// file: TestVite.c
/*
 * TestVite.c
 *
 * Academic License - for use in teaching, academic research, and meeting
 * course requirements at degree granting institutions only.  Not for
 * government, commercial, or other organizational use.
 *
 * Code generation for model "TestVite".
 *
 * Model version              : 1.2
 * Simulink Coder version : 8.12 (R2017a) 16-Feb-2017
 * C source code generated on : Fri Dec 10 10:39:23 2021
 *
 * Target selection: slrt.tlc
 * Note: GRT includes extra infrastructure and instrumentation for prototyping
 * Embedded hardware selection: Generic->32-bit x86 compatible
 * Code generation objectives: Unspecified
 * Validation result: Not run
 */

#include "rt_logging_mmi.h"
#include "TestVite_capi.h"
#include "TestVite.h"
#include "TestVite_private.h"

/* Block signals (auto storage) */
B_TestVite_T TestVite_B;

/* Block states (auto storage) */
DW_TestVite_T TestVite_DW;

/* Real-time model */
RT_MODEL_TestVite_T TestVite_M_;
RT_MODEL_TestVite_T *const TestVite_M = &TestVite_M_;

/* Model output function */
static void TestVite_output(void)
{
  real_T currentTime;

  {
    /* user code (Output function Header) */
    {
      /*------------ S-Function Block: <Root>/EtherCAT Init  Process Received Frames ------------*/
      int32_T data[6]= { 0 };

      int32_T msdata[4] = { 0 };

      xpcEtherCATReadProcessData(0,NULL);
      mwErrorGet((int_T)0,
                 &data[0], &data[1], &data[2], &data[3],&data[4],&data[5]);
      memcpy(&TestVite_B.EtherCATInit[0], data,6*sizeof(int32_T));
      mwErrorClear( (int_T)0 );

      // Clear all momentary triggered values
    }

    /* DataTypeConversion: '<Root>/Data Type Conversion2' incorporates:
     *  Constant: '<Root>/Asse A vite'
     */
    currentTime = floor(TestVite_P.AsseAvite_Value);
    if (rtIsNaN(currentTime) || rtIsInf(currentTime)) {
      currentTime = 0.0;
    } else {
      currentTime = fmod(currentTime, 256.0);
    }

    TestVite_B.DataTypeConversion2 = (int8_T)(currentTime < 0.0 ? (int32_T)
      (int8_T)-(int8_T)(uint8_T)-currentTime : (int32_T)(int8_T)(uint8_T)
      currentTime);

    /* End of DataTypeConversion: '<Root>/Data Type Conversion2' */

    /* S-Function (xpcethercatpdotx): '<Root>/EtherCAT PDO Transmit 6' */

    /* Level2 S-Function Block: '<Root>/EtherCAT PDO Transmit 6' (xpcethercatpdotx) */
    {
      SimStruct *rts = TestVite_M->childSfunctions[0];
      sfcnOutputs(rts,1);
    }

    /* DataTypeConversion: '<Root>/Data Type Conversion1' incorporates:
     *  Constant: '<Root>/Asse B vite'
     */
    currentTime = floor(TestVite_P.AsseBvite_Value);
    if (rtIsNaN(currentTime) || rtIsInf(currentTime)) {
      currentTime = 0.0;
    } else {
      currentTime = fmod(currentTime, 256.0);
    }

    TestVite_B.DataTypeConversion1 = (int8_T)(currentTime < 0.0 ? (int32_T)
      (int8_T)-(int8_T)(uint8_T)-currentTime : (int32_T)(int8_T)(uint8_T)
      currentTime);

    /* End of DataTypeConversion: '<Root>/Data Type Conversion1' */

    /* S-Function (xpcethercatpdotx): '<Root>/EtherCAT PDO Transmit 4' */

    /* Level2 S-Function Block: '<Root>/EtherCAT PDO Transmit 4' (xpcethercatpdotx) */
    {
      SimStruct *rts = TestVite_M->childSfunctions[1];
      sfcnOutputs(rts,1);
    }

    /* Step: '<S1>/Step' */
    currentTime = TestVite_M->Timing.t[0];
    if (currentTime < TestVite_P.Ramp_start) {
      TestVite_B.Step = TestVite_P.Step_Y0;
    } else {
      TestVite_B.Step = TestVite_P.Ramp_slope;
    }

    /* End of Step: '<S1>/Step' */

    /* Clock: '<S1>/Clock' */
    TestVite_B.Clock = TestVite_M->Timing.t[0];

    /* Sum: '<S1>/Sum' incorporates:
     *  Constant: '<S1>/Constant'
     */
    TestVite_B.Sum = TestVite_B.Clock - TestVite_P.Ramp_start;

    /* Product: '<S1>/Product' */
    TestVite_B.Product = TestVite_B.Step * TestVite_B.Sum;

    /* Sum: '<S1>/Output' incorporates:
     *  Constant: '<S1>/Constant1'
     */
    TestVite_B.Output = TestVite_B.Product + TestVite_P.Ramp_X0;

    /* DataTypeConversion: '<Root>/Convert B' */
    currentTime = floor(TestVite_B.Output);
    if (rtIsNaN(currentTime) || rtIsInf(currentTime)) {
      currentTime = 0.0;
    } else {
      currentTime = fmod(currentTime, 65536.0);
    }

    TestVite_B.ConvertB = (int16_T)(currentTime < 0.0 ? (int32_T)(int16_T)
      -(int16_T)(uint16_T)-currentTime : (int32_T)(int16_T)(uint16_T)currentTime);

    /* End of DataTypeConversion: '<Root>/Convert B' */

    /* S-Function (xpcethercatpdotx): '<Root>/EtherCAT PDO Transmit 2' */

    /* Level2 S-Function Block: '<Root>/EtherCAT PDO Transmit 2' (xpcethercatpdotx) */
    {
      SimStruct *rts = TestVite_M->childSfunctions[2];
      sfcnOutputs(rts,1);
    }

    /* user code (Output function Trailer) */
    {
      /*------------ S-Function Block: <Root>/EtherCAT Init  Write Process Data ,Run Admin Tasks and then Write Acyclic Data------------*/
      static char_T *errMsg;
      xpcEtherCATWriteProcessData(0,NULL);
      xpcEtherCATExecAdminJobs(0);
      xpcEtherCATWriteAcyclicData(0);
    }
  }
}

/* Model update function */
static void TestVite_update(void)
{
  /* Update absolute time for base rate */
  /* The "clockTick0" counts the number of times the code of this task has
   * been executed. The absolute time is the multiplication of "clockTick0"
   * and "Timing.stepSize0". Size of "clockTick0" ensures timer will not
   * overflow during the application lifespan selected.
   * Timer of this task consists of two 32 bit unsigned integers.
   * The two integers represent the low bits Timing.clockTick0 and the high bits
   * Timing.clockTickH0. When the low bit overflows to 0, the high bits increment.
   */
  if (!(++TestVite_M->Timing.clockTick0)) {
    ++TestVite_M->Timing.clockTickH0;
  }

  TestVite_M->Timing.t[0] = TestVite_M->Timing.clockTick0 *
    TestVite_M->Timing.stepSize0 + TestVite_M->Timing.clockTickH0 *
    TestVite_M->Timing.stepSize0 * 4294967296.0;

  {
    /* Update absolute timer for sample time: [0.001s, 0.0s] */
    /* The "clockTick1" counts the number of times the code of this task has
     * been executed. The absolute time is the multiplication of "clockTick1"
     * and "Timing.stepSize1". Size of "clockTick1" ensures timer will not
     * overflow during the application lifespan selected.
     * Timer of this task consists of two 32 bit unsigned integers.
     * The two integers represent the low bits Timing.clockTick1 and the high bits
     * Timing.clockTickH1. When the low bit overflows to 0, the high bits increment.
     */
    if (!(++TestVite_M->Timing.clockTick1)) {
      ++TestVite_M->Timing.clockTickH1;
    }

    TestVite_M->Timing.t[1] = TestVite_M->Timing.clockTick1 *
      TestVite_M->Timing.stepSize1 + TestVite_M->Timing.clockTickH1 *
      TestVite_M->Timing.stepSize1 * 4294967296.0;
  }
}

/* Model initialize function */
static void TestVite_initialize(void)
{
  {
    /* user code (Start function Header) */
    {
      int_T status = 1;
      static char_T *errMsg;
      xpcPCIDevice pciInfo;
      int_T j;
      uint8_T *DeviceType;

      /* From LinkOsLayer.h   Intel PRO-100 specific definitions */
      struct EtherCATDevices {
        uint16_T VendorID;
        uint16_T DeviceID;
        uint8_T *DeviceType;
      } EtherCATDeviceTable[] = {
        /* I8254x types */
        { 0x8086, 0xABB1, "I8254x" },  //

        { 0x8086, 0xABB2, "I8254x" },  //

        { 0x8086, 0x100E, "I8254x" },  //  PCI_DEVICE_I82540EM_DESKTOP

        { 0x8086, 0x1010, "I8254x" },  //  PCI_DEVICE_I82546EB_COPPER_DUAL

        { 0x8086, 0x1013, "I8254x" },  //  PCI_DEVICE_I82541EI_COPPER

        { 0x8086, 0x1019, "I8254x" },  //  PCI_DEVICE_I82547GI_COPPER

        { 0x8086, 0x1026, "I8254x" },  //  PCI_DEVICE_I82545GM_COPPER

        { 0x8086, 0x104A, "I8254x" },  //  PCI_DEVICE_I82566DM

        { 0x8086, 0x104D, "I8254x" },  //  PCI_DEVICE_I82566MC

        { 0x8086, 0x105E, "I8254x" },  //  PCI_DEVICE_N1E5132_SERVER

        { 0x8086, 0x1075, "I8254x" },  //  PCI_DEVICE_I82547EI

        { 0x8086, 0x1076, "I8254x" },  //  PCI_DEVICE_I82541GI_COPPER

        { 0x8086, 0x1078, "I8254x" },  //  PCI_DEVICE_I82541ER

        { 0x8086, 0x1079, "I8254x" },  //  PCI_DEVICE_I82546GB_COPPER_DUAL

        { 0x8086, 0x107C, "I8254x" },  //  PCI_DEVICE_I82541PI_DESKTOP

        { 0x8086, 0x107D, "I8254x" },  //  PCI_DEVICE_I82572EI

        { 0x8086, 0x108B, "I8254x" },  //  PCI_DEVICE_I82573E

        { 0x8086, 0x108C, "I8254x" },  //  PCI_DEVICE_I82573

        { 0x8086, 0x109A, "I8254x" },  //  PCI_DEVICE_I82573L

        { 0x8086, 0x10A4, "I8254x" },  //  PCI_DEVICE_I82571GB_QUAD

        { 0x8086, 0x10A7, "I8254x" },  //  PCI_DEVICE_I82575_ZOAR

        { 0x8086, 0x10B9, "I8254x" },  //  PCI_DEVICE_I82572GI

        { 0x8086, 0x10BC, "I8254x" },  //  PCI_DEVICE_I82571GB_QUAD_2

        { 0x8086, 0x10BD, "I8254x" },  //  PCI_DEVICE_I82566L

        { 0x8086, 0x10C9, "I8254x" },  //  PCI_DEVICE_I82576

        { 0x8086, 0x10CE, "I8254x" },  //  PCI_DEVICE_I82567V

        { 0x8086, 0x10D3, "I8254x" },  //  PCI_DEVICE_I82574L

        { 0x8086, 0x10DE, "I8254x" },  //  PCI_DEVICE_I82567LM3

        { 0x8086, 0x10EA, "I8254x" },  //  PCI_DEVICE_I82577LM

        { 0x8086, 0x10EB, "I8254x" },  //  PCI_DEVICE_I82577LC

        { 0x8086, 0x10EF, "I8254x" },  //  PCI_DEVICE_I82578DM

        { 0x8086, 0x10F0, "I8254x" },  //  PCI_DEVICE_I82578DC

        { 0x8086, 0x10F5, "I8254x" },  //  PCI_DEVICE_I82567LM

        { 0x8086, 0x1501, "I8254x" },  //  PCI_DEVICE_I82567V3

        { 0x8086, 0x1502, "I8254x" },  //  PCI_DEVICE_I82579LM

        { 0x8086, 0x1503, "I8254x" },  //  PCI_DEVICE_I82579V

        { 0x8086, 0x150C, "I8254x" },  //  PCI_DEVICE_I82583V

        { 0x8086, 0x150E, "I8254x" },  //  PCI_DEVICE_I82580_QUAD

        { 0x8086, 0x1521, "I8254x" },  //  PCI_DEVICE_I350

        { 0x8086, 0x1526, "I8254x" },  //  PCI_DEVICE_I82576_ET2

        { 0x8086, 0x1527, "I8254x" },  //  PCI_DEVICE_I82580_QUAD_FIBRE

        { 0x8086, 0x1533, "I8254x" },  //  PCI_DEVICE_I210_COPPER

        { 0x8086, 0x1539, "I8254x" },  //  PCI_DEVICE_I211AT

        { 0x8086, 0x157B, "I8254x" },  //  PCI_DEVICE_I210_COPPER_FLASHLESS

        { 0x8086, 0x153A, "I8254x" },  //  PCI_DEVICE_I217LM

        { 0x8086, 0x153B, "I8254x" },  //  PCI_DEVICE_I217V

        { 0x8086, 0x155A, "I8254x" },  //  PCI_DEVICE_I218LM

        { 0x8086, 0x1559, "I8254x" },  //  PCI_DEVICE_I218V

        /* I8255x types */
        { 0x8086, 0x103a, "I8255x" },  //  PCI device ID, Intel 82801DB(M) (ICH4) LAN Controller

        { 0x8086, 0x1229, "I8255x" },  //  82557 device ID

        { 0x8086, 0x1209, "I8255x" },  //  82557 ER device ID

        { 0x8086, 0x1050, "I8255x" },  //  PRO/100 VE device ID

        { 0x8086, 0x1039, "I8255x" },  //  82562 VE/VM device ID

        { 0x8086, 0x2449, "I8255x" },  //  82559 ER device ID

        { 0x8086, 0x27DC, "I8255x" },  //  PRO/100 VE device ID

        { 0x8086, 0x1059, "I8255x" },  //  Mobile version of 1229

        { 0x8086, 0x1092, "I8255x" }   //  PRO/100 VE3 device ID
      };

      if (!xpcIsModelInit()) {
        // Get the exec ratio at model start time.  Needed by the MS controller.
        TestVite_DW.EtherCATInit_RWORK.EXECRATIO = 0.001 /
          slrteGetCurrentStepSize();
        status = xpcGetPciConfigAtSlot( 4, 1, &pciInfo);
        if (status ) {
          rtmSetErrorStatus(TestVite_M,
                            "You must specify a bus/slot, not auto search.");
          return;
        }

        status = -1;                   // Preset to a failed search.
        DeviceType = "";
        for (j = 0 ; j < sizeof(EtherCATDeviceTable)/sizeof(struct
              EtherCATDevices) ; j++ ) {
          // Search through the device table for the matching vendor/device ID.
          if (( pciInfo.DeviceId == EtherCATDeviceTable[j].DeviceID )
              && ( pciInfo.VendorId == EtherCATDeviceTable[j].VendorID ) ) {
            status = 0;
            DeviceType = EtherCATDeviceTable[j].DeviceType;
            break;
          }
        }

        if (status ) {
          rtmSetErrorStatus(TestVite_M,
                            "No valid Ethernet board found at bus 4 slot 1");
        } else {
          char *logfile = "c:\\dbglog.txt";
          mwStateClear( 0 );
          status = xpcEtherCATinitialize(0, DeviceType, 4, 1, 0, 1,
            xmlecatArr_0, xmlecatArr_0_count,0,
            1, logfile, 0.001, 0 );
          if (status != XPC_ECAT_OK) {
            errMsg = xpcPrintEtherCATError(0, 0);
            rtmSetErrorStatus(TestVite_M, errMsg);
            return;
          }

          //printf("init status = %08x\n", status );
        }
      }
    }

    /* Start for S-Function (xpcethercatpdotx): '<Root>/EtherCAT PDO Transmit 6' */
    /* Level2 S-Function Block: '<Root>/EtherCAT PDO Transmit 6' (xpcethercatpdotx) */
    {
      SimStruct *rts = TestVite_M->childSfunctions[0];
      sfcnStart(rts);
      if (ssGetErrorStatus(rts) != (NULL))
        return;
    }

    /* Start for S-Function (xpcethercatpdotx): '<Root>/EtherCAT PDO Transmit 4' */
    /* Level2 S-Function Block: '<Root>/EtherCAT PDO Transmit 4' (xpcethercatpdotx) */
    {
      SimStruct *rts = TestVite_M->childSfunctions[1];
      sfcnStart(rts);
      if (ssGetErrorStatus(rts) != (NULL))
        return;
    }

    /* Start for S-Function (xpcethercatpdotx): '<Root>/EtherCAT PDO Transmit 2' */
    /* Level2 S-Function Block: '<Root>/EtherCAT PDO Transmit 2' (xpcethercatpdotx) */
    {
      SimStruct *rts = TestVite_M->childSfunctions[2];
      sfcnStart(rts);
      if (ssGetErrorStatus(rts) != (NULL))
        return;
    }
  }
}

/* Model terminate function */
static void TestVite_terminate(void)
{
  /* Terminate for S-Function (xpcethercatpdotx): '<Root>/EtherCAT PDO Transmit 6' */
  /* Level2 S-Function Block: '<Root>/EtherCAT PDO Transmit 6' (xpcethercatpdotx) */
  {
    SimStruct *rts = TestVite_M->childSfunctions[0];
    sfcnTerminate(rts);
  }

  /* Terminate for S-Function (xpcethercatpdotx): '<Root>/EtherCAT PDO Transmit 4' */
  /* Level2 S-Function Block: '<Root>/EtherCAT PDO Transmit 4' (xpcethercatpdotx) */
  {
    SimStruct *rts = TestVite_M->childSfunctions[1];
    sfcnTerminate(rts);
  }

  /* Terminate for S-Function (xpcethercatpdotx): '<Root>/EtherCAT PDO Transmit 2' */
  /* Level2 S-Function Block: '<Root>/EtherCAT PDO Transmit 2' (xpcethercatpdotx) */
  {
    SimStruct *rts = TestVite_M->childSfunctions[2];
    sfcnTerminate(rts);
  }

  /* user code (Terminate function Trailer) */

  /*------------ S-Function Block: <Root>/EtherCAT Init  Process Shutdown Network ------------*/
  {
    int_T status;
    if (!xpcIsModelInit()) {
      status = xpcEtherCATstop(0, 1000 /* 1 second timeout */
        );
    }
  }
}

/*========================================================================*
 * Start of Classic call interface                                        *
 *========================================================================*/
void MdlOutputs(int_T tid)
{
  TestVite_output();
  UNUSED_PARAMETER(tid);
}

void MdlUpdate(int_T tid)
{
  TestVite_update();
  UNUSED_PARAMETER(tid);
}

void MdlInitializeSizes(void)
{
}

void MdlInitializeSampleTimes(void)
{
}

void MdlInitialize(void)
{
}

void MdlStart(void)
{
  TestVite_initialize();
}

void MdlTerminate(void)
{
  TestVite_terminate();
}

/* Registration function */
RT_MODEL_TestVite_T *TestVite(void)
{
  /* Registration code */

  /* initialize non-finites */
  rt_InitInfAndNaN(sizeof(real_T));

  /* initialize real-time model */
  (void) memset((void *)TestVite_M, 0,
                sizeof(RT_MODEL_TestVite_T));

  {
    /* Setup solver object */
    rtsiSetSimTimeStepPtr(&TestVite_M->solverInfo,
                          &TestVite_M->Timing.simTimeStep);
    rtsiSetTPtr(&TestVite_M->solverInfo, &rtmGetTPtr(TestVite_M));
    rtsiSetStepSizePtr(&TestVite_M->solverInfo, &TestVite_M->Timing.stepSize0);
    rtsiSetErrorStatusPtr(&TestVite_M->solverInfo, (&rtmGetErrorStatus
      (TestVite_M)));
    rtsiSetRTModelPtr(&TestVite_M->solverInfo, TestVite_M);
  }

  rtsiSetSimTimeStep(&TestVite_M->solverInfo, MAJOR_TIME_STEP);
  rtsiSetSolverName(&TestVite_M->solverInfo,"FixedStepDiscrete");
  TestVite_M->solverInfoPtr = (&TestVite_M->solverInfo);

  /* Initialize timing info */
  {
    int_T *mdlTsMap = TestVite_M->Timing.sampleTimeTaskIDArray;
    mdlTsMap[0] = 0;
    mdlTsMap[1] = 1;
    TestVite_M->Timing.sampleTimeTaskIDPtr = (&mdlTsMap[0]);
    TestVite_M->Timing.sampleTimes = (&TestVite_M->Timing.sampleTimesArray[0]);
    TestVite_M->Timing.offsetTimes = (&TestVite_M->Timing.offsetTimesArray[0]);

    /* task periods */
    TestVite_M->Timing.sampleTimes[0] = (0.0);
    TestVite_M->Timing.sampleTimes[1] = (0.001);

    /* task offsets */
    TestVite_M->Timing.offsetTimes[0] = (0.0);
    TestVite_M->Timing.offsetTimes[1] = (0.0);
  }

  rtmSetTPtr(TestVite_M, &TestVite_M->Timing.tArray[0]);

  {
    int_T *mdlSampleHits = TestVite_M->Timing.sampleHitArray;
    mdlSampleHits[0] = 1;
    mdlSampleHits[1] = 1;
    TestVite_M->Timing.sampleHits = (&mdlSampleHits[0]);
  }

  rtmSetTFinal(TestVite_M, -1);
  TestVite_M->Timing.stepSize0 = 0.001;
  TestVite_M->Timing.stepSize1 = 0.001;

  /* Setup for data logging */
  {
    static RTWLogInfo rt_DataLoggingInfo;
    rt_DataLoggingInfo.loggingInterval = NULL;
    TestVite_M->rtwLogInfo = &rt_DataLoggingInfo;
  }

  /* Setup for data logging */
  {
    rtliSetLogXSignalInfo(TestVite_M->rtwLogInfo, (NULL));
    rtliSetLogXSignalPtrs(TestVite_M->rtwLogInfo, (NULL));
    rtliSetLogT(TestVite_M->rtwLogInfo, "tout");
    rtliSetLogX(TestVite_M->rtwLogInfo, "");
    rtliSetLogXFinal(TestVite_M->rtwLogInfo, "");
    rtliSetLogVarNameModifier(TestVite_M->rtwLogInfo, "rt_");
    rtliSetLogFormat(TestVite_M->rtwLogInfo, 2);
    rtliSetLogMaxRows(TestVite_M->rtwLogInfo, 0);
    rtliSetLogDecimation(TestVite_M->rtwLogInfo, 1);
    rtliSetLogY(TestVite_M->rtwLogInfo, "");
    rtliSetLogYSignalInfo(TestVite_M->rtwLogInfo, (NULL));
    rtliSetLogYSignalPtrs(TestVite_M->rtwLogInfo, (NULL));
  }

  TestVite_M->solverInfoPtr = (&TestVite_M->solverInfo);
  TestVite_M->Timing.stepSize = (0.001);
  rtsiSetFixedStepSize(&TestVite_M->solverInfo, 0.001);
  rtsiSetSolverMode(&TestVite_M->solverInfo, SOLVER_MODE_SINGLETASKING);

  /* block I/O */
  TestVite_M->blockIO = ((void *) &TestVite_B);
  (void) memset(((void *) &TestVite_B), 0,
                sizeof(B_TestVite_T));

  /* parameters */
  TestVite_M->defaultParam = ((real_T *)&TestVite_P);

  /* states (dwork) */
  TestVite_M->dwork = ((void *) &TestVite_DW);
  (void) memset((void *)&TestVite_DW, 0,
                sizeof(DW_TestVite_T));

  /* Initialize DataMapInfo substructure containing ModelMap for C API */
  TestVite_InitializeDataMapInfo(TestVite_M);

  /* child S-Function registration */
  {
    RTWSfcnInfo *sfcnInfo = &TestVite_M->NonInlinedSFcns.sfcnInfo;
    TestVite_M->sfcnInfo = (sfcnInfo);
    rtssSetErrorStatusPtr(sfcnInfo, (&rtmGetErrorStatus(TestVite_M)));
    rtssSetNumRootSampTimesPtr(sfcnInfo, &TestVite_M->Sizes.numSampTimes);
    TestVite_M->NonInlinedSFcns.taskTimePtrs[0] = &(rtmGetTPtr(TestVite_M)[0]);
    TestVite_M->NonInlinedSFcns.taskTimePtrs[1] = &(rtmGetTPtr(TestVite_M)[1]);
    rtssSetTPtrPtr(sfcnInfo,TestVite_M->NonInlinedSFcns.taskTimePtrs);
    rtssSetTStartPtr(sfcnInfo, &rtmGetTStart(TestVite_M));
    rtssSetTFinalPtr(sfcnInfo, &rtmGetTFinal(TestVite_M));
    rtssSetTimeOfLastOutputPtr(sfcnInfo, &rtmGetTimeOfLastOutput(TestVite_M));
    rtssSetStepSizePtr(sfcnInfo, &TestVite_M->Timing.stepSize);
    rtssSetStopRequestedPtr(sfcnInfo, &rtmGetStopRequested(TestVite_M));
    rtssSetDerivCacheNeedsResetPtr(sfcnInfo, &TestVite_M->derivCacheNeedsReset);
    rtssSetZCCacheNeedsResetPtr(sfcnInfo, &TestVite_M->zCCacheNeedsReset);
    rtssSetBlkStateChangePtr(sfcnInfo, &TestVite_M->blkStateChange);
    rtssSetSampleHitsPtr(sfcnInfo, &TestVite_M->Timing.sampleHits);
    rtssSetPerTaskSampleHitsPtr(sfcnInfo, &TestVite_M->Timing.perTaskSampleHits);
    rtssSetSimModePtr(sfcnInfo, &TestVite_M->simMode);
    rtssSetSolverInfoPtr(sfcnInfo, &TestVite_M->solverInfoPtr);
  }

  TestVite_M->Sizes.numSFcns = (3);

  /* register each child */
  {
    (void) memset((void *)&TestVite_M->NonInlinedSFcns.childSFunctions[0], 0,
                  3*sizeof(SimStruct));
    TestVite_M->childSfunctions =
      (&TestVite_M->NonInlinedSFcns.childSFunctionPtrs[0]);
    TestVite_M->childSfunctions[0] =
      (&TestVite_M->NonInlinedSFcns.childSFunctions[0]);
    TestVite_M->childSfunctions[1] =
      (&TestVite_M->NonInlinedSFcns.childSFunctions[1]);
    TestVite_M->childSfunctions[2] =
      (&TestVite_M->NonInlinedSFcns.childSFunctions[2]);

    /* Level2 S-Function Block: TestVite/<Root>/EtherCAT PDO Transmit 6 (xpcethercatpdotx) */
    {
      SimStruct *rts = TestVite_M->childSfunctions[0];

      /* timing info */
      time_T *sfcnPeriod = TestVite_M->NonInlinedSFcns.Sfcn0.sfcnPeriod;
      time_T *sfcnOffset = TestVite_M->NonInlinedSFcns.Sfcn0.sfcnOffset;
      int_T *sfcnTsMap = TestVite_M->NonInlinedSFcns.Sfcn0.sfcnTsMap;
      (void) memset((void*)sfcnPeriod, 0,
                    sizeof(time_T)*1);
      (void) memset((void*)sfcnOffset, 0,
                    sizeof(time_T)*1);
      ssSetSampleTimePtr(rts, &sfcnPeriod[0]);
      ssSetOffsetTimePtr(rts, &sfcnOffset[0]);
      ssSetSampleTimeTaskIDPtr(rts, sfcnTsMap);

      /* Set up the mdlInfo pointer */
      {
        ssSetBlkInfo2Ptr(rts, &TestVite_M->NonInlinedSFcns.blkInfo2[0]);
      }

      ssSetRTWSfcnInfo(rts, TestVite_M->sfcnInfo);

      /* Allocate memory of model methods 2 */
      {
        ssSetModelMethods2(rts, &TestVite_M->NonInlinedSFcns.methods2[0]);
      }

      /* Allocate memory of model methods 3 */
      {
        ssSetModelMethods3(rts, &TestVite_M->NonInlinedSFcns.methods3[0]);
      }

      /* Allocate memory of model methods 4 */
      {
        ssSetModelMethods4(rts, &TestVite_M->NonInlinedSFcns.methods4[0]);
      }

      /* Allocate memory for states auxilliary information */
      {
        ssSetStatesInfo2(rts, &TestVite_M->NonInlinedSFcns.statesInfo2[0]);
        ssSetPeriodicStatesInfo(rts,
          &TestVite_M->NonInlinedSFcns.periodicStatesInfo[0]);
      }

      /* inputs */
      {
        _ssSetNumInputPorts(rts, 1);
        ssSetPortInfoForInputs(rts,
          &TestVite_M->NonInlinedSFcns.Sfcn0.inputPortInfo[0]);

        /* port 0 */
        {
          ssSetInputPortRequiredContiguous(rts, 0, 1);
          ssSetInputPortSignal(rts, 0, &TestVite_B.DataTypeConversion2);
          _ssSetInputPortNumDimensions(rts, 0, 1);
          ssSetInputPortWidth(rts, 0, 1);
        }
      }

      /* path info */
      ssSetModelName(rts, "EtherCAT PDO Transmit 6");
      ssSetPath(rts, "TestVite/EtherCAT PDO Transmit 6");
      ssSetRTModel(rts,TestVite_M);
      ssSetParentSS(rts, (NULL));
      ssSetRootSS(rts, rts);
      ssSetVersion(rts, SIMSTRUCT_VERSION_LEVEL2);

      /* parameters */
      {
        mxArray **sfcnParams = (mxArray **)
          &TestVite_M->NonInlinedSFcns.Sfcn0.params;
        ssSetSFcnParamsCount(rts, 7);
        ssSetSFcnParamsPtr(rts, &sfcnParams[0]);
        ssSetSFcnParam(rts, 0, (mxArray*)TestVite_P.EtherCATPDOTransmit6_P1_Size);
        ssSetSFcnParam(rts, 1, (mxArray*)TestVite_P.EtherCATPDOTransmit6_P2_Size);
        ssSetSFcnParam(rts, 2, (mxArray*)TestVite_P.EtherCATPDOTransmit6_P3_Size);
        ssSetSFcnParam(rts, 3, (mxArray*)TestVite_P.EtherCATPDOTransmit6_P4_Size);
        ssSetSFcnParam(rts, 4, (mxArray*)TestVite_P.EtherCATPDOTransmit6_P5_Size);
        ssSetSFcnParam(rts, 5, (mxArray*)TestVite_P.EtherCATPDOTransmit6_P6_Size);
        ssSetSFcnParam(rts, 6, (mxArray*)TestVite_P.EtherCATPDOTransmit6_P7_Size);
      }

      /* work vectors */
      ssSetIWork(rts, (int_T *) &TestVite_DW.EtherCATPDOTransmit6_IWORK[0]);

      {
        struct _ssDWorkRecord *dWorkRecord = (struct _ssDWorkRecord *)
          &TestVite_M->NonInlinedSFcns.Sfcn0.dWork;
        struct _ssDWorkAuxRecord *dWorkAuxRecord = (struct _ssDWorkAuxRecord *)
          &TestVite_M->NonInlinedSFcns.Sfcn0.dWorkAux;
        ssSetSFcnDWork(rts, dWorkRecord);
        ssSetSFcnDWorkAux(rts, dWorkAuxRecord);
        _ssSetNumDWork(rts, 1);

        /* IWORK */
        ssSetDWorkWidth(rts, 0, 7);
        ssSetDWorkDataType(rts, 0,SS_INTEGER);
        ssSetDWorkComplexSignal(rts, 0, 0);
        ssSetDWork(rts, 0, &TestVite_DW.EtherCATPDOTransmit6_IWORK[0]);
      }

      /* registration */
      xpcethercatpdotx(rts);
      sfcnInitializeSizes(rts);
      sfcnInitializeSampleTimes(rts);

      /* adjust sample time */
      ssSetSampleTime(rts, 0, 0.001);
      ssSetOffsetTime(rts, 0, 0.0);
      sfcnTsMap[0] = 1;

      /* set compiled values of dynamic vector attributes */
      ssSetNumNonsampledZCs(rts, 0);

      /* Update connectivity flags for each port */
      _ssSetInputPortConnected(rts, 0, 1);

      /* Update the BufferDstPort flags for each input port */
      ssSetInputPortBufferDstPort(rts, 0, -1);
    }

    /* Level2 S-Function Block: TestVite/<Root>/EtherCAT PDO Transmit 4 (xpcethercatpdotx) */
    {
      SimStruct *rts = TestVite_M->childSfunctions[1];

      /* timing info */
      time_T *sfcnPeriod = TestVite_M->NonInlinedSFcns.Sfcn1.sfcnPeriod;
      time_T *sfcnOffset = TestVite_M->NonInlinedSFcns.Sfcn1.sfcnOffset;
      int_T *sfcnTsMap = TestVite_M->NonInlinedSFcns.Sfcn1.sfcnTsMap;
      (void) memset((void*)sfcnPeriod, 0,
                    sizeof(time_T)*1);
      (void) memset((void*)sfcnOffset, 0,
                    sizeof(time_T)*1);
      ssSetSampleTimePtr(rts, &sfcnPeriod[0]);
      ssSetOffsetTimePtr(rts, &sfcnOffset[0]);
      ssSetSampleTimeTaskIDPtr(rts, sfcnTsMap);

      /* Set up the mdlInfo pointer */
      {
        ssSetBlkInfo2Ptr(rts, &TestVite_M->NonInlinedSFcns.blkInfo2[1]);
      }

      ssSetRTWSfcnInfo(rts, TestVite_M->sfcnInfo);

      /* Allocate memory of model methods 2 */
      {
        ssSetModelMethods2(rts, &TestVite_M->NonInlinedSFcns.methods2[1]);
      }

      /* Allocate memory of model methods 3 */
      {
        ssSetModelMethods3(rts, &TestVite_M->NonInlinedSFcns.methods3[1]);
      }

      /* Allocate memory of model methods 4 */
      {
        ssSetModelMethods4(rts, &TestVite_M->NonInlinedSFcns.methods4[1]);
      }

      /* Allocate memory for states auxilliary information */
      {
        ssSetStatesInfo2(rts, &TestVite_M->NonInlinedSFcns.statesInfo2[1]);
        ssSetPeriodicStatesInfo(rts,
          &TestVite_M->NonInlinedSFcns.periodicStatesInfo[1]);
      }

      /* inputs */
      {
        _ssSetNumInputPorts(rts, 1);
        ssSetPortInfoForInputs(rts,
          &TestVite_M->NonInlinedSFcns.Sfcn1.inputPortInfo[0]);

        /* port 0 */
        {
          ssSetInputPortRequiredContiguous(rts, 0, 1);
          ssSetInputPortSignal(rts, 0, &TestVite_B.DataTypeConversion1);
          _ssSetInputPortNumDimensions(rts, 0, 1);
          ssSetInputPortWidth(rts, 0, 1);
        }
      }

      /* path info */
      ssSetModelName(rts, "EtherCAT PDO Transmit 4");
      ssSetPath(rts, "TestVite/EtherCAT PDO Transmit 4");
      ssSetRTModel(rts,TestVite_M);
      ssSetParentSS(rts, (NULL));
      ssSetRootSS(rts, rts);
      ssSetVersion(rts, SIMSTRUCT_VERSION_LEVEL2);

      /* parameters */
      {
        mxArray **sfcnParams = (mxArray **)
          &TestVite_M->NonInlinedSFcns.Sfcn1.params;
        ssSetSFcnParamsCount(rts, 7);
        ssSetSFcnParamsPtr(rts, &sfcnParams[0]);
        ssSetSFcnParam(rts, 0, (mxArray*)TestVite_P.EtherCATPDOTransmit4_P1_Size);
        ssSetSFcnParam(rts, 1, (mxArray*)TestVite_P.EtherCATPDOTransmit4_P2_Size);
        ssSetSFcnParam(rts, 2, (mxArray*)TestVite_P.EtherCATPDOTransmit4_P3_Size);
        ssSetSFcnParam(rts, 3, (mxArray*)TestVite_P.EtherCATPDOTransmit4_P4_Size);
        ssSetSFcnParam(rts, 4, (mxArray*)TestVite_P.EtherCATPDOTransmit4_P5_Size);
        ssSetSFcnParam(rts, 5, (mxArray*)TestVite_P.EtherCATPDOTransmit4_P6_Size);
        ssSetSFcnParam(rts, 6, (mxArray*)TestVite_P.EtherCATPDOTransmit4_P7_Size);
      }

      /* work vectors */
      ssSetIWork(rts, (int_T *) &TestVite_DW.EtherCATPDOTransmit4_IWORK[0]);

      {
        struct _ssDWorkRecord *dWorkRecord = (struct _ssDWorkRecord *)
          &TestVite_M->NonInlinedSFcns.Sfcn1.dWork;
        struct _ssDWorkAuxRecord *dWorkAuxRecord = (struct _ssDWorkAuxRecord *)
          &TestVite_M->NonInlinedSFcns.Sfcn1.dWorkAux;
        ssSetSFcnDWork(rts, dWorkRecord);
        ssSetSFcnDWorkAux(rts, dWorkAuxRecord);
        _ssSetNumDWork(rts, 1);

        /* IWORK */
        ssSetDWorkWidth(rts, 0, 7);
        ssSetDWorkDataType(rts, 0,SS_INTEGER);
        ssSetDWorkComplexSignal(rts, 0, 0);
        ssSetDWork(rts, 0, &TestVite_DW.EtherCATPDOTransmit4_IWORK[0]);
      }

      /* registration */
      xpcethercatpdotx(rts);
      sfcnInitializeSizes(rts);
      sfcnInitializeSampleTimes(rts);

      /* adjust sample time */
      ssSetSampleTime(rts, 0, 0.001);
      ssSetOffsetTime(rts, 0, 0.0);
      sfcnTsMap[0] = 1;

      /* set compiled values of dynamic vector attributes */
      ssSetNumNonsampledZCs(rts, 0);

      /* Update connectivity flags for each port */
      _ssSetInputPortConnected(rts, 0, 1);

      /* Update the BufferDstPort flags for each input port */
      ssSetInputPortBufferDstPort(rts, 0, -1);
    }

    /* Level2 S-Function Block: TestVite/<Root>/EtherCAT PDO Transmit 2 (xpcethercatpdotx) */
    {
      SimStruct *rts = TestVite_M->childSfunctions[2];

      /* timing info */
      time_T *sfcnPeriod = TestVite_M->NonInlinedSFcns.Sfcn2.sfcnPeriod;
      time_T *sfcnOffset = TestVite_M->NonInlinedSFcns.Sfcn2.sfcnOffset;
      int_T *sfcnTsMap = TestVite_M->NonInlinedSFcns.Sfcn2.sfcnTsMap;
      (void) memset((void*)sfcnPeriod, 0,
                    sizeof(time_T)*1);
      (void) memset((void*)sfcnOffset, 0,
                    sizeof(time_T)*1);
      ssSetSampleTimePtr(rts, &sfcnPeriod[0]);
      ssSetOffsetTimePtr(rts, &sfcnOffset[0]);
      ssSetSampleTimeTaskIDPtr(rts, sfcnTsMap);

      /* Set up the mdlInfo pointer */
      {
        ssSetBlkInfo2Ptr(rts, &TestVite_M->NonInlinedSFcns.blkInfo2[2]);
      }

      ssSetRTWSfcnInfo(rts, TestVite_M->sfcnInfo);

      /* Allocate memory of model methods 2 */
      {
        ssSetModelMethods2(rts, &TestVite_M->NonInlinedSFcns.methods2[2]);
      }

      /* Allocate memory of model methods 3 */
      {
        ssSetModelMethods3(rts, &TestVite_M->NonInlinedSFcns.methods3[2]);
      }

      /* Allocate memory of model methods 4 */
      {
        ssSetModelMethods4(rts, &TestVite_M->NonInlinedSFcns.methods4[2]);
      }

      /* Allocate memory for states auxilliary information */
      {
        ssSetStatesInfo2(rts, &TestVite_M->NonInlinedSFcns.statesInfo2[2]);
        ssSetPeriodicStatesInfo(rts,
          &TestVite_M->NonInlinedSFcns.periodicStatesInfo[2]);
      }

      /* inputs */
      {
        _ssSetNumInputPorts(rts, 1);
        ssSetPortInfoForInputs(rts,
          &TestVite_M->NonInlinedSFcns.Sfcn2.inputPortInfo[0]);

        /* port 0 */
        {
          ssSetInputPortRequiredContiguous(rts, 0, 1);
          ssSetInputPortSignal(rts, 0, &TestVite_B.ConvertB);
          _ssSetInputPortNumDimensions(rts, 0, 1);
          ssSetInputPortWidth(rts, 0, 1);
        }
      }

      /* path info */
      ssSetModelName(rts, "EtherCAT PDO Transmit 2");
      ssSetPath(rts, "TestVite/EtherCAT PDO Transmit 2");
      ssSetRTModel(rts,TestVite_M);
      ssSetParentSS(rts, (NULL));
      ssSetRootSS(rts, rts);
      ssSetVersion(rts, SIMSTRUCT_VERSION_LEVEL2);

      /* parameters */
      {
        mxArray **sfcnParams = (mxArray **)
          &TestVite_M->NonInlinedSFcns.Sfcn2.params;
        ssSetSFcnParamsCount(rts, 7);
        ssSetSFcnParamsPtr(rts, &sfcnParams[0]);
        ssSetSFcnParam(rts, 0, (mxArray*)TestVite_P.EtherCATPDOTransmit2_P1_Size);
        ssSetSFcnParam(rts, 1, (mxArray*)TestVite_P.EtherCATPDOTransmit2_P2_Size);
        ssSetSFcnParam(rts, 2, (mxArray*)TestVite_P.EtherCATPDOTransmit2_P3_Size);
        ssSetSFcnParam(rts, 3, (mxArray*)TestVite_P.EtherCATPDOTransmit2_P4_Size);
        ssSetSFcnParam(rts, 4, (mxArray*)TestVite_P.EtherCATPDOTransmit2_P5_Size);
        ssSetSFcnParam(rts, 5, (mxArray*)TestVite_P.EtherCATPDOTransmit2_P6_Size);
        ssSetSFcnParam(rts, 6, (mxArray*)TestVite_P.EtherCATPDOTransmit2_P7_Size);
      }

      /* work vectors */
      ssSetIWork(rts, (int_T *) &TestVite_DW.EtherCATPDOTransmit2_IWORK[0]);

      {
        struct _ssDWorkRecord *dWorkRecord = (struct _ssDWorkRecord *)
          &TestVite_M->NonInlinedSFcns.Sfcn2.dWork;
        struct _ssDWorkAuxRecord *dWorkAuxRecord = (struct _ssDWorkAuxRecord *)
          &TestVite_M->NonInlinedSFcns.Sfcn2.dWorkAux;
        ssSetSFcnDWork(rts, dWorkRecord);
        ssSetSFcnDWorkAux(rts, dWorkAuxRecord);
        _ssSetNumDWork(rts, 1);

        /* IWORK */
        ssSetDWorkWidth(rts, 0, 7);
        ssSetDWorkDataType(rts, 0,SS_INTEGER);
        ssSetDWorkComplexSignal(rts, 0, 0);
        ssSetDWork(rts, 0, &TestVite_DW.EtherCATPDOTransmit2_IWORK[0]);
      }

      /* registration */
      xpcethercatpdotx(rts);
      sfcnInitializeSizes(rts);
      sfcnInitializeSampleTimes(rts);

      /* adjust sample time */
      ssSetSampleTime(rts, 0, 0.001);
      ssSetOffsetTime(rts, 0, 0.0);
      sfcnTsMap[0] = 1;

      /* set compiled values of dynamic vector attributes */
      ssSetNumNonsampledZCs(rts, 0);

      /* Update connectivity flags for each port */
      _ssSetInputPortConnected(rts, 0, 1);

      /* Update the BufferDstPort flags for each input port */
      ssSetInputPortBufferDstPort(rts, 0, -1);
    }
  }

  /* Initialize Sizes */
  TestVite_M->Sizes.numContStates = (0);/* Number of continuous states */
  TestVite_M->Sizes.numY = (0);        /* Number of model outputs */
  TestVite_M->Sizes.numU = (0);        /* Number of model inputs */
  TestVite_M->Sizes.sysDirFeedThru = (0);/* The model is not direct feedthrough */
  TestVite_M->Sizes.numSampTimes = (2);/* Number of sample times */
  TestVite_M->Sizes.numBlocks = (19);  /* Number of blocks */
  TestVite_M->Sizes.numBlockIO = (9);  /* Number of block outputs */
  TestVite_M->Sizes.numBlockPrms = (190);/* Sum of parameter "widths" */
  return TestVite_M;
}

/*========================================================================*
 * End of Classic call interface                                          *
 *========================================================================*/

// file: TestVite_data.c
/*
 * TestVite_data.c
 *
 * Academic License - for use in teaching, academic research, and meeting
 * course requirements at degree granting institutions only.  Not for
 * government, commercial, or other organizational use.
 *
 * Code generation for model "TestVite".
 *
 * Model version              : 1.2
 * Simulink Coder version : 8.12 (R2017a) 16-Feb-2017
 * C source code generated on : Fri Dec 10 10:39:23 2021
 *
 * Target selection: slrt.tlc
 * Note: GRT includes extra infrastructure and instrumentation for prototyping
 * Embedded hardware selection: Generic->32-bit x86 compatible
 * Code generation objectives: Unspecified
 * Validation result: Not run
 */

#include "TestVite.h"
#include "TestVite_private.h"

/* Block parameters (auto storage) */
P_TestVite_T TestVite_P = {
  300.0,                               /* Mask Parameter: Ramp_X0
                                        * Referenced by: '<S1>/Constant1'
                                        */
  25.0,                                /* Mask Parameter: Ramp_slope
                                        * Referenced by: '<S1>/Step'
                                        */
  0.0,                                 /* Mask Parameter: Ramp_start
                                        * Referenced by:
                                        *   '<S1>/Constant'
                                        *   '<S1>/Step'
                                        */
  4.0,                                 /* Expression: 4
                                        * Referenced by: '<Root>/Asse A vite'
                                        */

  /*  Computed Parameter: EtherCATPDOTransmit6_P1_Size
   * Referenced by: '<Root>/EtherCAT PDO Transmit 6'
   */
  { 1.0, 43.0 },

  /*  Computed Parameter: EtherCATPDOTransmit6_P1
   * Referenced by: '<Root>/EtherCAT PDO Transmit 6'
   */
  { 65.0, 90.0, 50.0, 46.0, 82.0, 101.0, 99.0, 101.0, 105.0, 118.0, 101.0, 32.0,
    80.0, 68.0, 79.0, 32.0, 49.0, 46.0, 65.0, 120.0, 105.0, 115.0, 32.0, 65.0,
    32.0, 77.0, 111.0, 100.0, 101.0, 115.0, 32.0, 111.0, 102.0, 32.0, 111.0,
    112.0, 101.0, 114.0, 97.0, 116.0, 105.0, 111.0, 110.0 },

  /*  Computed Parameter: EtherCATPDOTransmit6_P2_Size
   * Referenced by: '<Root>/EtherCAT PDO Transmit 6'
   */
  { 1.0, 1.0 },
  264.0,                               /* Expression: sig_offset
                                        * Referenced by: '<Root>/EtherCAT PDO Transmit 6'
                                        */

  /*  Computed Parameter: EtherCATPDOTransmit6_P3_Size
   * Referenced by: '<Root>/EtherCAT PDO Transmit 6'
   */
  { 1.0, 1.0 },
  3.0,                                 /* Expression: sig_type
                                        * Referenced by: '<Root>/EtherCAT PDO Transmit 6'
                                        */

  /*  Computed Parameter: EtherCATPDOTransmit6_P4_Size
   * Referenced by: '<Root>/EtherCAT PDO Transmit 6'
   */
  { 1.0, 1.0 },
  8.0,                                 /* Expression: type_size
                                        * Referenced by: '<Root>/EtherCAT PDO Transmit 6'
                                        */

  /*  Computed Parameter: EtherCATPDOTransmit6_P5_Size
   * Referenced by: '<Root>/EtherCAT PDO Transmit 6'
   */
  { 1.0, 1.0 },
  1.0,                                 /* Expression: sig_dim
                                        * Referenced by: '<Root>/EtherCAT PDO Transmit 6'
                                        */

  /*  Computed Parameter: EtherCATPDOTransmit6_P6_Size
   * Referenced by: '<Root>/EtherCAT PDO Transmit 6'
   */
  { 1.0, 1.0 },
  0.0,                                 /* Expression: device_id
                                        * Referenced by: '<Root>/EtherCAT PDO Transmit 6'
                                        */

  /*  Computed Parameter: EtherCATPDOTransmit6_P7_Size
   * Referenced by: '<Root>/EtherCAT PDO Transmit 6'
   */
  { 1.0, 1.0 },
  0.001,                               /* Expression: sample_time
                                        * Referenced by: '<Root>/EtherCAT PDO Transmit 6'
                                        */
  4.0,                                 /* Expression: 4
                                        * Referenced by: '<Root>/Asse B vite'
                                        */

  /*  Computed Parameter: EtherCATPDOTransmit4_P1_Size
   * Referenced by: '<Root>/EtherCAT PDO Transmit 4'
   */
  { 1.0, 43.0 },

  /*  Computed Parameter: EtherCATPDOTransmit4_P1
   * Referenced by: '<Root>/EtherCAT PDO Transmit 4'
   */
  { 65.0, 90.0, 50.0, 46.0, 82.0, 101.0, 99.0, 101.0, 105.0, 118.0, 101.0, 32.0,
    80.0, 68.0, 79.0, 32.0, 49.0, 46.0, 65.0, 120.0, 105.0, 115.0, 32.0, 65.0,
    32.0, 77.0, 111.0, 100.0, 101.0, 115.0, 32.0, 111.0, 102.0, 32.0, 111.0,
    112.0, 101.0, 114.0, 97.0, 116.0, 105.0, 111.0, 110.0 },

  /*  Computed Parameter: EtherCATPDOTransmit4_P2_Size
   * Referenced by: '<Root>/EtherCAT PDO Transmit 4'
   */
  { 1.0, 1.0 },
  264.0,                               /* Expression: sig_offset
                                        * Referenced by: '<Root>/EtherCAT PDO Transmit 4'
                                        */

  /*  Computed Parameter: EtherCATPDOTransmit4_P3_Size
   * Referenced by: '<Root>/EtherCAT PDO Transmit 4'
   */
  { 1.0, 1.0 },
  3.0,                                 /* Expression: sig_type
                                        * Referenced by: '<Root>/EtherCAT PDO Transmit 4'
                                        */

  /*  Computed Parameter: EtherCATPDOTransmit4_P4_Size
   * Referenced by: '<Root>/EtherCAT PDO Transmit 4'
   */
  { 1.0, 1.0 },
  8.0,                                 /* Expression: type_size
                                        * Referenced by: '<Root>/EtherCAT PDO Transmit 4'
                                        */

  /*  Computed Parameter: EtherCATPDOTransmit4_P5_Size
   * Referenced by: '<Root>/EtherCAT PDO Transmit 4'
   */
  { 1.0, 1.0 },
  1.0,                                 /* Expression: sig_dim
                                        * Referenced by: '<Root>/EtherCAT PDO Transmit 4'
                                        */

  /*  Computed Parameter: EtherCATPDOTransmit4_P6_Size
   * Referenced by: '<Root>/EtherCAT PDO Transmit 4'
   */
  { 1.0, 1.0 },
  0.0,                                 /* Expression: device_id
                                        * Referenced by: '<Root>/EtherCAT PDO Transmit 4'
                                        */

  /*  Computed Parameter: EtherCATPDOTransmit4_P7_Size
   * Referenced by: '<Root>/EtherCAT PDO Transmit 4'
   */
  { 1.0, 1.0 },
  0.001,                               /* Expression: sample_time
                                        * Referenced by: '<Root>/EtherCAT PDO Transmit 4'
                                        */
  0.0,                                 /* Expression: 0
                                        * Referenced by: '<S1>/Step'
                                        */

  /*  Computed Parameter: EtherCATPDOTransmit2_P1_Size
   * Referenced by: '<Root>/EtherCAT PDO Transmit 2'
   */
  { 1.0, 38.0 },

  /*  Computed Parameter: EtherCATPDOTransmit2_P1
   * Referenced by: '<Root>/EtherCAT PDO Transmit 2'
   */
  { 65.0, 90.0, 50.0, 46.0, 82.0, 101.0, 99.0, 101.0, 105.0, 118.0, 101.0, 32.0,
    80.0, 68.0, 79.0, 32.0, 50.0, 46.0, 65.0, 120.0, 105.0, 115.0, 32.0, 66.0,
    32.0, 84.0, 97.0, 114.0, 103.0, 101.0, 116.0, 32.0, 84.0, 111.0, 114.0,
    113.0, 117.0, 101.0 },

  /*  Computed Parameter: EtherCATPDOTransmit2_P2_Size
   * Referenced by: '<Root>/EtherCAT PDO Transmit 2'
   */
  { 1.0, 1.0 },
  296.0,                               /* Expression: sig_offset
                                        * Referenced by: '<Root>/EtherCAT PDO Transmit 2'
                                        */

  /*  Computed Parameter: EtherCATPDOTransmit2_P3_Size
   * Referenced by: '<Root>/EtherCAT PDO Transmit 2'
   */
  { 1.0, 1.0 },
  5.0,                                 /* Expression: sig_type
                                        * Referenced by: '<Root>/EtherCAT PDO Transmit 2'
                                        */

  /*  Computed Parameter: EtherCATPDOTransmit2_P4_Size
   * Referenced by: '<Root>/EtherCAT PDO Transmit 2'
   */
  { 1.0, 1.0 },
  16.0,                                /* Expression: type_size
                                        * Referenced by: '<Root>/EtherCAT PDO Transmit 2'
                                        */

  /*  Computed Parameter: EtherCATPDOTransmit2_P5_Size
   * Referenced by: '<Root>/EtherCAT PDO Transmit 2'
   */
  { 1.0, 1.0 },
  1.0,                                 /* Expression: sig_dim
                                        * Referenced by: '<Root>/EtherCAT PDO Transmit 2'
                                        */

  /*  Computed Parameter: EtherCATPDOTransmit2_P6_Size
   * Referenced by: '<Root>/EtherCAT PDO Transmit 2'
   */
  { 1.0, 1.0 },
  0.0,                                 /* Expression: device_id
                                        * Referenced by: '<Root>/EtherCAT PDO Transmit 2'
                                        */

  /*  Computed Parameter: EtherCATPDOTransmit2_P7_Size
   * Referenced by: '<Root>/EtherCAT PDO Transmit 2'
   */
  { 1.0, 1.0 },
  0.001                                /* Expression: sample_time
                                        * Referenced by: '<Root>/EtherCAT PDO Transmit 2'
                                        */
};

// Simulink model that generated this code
simulink model "TestVite"  (R2017a)
settings: Solver=FixedStepDiscrete  StartTime=0.0  StopTime=inf  FixedStep=0.001  RelTol=1e-3  EnableMultiTasking=on
values from neighbouring files (symbols this model uses):
  C = B    [testMatricePiccola.m]
libraries: xpcethercatlib x4, simulink x1

== system TestVite ==
  note: Asse B Vite
  Asse A vite : Constant  Value=4
  Asse B vite : Constant  Value=4
  Convert B : DataTypeConversion
  Data Type Conversion1 : DataTypeConversion
  Data Type Conversion2 : DataTypeConversion
  Display : Display
  "EtherCAT Init " : xpcethercatlib/EtherCAT Init   Priority=0  config_file=C:\Users\Danie\Documenti\MATLAB\PKMRobot\final_net.xml  device_id=0  pci_bus=4  pci_slot=1  dctuning=0  enaDebug=off  enaDC=on  errLink=off  masterDbg=off  stateChgDbg=off  baseClock=off  masterCfg=off  logFile='c:\dbglog.txt'  sample_time=0.001000  DCMode=1
  EtherCAT PDO Transmit 2 : xpcethercatlib/EtherCAT PDO Transmit   Priority=3  sig_name=AZ2.Receive PDO 2.Axis B Target Torque  sig_offset=296  sig_type=int16  type_size=16  sig_dim=1  device_id=0  sample_time=0.001000
  EtherCAT PDO Transmit 4 : xpcethercatlib/EtherCAT PDO Transmit   Priority=3  sig_name=AZ2.Receive PDO 1.Axis A Modes of operation  sig_offset=264  sig_type=int8  type_size=8  sig_dim=1  device_id=0  sample_time=0.001000
  EtherCAT PDO Transmit 6 : xpcethercatlib/EtherCAT PDO Transmit   Priority=3  sig_name=AZ2.Receive PDO 1.Axis A Modes of operation  sig_offset=264  sig_type=int8  type_size=8  sig_dim=1  device_id=0  sample_time=0.001000
  Ramp : simulink/Sources/Ramp  slope=25  start=0  X0=300
  wires:
  Ramp/1 -> Convert B/1
  Convert B/1 -> EtherCAT PDO Transmit 2/1
  Asse A vite/1 -> Data Type Conversion2/1
  Data Type Conversion2/1 -> EtherCAT PDO Transmit 6/1
  Asse B vite/1 -> Data Type Conversion1/1
  Data Type Conversion1/1 -> EtherCAT PDO Transmit 4/1
  "EtherCAT Init "/1 -> Display/1
